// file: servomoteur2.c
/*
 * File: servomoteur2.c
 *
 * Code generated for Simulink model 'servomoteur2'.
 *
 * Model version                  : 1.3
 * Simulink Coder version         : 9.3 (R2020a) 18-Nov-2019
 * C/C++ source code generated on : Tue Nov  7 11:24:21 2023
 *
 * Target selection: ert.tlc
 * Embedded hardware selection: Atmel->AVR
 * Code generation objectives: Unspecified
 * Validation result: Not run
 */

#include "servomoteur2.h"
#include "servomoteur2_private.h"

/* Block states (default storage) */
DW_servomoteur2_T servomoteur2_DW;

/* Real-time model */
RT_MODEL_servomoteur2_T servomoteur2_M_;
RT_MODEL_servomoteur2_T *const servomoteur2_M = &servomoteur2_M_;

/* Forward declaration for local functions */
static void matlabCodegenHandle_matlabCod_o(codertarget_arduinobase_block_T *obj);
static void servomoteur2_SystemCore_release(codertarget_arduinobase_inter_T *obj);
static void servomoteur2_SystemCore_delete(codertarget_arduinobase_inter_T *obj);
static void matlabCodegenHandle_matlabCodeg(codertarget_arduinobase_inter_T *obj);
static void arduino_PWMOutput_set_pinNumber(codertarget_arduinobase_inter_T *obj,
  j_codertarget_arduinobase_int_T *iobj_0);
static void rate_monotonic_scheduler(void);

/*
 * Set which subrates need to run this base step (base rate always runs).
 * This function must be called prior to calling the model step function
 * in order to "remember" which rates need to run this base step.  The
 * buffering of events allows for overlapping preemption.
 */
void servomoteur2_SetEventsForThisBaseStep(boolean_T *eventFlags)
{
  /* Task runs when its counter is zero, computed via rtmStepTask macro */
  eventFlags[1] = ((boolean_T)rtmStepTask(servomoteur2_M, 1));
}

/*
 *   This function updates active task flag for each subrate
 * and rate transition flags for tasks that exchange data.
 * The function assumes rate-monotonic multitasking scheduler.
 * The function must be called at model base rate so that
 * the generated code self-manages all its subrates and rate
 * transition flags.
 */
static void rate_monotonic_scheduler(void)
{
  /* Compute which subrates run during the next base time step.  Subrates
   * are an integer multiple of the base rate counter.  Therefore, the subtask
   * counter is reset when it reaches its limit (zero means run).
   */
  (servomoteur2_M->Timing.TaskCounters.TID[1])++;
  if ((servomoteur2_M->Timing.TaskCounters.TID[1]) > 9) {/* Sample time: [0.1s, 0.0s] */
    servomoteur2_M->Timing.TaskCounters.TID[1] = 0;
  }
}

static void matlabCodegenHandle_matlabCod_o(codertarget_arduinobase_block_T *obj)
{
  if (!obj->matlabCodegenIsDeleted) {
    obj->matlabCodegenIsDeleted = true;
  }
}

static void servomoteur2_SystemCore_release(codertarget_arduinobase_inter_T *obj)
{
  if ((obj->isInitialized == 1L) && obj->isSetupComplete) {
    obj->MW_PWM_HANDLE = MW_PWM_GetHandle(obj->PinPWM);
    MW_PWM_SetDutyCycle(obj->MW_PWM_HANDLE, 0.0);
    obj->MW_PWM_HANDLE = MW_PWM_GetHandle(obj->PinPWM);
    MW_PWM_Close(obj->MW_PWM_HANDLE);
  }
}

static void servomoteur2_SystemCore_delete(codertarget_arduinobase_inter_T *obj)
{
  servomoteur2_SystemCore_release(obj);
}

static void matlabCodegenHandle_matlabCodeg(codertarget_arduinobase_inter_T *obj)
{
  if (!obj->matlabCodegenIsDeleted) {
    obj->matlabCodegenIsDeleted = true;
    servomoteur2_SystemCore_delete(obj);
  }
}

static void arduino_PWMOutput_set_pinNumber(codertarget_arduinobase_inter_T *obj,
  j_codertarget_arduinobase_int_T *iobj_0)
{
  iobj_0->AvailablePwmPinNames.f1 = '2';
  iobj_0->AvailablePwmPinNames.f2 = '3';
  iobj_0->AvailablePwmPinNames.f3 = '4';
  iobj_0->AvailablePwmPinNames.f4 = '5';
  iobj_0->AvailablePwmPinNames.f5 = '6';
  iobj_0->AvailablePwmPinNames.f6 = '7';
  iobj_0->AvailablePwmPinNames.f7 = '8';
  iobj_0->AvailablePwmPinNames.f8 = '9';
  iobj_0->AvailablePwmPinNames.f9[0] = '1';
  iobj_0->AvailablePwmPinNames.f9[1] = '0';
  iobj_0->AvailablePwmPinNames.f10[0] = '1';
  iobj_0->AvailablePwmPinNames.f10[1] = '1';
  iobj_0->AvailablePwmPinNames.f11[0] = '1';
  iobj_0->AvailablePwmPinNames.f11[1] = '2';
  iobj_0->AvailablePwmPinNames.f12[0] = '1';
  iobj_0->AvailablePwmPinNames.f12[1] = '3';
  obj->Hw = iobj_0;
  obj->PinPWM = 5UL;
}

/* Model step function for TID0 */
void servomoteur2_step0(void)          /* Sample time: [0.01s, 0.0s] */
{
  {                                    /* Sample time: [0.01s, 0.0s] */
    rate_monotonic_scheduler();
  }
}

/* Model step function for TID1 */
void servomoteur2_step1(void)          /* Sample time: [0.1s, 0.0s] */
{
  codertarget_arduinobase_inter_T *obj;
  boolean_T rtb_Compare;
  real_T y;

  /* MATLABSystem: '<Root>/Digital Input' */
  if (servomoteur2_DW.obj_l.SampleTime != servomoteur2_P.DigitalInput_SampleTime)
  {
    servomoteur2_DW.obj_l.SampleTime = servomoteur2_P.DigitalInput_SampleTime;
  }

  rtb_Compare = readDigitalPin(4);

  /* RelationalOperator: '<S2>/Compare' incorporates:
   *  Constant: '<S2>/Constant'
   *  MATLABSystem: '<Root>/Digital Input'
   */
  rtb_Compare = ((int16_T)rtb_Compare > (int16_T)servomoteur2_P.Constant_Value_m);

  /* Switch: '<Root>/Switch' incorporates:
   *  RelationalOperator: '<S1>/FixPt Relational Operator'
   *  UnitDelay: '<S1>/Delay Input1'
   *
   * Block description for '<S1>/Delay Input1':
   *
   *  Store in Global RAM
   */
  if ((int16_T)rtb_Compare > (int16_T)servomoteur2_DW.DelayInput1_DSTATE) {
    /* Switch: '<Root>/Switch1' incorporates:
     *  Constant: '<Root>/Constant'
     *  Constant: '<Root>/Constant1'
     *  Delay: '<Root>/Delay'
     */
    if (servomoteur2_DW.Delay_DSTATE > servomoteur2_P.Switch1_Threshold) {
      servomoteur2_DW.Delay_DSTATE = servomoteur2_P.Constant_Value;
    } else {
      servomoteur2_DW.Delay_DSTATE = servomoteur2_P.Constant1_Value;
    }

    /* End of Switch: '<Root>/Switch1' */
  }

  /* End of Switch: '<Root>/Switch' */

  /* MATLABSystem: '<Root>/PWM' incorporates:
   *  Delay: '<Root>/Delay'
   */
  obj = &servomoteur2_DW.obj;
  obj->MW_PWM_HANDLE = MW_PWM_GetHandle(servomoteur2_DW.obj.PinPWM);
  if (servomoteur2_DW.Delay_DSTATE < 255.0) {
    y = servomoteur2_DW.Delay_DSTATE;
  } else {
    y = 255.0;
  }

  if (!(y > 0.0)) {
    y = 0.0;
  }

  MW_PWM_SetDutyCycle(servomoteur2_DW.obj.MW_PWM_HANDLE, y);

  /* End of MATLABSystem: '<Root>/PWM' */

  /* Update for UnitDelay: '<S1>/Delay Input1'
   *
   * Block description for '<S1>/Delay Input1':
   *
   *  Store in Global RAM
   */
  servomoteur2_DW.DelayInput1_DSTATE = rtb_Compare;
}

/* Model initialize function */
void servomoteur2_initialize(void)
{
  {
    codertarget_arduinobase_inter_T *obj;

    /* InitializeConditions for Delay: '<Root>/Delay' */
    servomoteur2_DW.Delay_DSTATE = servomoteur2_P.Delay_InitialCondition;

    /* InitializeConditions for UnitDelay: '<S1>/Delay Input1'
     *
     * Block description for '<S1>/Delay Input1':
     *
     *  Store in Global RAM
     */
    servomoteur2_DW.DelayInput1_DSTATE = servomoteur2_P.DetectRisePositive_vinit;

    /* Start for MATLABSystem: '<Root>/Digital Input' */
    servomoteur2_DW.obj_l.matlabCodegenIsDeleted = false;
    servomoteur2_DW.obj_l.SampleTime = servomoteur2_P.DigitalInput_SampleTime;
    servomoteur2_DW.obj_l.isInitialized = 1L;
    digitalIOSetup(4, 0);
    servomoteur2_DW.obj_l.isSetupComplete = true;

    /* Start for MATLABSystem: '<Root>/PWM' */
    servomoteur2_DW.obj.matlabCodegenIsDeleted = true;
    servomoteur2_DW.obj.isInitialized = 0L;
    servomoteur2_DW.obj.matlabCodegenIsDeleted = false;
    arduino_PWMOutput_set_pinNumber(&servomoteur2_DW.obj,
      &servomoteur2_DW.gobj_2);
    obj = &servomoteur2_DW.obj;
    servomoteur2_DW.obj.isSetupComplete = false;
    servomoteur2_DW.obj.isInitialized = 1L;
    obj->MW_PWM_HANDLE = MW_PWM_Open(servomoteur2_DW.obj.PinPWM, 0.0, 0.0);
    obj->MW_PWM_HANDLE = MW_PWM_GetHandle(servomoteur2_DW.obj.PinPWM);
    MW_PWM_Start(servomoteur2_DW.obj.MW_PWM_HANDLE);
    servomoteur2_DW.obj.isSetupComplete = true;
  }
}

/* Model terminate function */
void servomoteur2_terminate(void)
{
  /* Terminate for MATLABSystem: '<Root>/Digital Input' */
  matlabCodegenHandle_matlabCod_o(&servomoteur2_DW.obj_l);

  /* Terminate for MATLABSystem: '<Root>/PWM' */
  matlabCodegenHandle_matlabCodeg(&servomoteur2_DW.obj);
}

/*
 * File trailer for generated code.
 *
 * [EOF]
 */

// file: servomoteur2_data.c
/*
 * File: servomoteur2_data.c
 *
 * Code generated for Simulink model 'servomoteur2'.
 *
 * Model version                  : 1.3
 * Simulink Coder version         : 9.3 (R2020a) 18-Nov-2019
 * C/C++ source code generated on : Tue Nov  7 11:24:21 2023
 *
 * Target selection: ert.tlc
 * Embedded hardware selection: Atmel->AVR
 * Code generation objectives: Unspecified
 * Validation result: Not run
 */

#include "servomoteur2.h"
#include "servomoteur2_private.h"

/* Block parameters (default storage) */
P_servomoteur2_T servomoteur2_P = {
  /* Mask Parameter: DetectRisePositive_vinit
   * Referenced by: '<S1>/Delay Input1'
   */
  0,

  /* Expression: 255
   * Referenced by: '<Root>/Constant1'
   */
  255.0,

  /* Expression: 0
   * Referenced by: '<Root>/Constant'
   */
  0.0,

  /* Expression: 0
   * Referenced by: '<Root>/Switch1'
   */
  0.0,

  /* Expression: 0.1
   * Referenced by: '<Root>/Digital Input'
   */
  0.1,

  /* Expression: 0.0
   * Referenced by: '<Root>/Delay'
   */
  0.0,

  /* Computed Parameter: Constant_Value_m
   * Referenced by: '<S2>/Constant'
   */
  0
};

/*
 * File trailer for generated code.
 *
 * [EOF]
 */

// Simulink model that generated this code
simulink model "servomoteur2"  (R2020a)
settings: Solver=FixedStepDiscrete  StartTime=0.0  StopTime=10.0  FixedStep=0.01  RelTol=1e-3  EnableMultiTasking=on
libraries: arduinolib x2, simulink x1

== system servomoteur2 ==
  Constant : Constant  Value=0
  Constant1 : Constant  Value=255
  Delay : Delay  DelayLength=1
  Detect Rise Positive : simulink/Logic and Bit Operations/Detect Rise Positive  vinit=0  OutDataTypeStr=boolean
  Digital Input : arduinolib/Digital Input  pinNumber=4  Direction=input  SampleTime=0.1  blockPlatform=arduino
  PWM : arduinolib/PWM  pinNumber=5  frequencyType=Default  desiredFrequency=490.2  achievableFrequency=490.2
  Switch : Switch  Criteria=u2 > Threshold
  Switch1 : Switch  Criteria=u2 > Threshold
  wires:
  Detect Rise Positive/1 -> Switch/2
  Switch1/1 -> Switch/1
  Digital Input/1 -> Detect Rise Positive/1
  Constant1/1 -> Switch1/3
  Constant/1 -> Switch1/1
  Switch/1 -> PWM/1, Delay/1
  Delay/1 -> Switch/3, Switch1/2
